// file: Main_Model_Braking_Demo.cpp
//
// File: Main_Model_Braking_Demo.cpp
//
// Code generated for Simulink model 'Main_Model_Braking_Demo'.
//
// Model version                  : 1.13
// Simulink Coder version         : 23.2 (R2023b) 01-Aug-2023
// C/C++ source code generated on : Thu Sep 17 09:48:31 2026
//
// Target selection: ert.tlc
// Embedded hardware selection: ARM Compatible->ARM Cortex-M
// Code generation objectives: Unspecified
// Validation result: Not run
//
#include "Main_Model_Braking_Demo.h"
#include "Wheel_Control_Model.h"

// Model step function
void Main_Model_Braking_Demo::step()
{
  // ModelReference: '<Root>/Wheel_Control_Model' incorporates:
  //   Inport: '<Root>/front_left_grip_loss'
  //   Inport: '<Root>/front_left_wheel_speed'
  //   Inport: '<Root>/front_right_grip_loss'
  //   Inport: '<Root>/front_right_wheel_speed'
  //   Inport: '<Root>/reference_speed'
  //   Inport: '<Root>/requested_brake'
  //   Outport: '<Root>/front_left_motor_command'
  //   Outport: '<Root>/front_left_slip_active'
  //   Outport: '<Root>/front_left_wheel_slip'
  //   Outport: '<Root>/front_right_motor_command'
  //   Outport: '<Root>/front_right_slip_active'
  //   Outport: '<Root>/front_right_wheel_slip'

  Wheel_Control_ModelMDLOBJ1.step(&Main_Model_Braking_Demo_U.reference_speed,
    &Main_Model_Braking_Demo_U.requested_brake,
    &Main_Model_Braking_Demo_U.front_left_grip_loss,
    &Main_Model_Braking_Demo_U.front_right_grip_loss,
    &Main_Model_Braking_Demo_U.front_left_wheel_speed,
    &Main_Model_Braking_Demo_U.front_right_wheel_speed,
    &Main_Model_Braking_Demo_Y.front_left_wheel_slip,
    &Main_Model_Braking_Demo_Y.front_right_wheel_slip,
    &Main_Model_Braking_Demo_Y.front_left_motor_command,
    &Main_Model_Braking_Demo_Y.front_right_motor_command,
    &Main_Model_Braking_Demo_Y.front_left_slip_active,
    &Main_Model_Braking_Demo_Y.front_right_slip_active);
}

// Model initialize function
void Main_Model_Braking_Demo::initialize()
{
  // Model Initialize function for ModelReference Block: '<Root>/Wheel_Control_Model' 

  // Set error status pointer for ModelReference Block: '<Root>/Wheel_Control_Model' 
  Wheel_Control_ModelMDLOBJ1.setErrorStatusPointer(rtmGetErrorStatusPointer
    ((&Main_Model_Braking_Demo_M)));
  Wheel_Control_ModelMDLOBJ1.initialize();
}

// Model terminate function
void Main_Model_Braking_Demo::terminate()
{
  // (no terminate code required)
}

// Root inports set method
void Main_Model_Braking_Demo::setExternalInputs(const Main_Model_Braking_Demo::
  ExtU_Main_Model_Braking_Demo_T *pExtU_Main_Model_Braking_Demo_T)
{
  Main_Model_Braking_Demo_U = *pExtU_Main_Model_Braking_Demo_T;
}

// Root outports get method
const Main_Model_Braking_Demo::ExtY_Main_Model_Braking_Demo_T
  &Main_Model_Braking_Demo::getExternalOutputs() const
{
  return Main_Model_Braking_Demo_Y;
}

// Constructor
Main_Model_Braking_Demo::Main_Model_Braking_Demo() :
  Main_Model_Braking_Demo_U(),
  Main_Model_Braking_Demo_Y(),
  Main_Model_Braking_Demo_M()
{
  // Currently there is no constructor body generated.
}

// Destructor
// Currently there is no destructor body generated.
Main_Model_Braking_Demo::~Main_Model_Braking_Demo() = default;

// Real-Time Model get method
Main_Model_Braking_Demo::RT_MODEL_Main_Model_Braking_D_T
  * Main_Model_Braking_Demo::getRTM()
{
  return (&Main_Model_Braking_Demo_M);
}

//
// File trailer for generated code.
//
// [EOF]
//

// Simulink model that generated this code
simulink model "Main_Model_Braking_Demo"  (R2023b)
settings: Solver=FixedStepDiscrete  StartTime=0.0  StopTime=10.0  RelTol=1e-3

== system Main_Model_Braking_Demo ==
  reference_speed : Inport  OutDataTypeStr=uint16
  requested_brake : Inport  Port=2  OutDataTypeStr=uint16
  front_left_grip_loss : Inport  Port=3  OutDataTypeStr=uint16
  front_right_grip_loss : Inport  Port=4  OutDataTypeStr=uint16
  front_left_wheel_speed : Inport  Port=5  OutDataTypeStr=uint16
  front_right_wheel_speed : Inport  Port=6  OutDataTypeStr=uint16
  Wheel_Control_Model : ModelReference  ModelNameDialog=Wheel_Control_Model.slx  SimulationMode=Normal  ModelReferenceVersion=1.14
  front_left_wheel_slip : Outport  OutDataTypeStr=uint16
  front_right_wheel_slip : Outport  Port=2  OutDataTypeStr=uint16
  front_left_motor_command : Outport  Port=3  OutDataTypeStr=uint16
  front_right_motor_command : Outport  Port=4  OutDataTypeStr=uint16
  front_left_slip_active : Outport  Port=5  OutDataTypeStr=boolean
  front_right_slip_active : Outport  Port=6  OutDataTypeStr=boolean
  wires:
  reference_speed/1 -> Wheel_Control_Model/1
  requested_brake/1 -> Wheel_Control_Model/2
  front_left_grip_loss/1 -> Wheel_Control_Model/3
  front_right_grip_loss/1 -> Wheel_Control_Model/4
  front_left_wheel_speed/1 -> Wheel_Control_Model/5
  front_right_wheel_speed/1 -> Wheel_Control_Model/6
  Wheel_Control_Model/1 -> front_left_wheel_slip/1
  Wheel_Control_Model/2 -> front_right_wheel_slip/1
  Wheel_Control_Model/3 -> front_left_motor_command/1
  Wheel_Control_Model/4 -> front_right_motor_command/1
  Wheel_Control_Model/5 -> front_left_slip_active/1
  Wheel_Control_Model/6 -> front_right_slip_active/1
